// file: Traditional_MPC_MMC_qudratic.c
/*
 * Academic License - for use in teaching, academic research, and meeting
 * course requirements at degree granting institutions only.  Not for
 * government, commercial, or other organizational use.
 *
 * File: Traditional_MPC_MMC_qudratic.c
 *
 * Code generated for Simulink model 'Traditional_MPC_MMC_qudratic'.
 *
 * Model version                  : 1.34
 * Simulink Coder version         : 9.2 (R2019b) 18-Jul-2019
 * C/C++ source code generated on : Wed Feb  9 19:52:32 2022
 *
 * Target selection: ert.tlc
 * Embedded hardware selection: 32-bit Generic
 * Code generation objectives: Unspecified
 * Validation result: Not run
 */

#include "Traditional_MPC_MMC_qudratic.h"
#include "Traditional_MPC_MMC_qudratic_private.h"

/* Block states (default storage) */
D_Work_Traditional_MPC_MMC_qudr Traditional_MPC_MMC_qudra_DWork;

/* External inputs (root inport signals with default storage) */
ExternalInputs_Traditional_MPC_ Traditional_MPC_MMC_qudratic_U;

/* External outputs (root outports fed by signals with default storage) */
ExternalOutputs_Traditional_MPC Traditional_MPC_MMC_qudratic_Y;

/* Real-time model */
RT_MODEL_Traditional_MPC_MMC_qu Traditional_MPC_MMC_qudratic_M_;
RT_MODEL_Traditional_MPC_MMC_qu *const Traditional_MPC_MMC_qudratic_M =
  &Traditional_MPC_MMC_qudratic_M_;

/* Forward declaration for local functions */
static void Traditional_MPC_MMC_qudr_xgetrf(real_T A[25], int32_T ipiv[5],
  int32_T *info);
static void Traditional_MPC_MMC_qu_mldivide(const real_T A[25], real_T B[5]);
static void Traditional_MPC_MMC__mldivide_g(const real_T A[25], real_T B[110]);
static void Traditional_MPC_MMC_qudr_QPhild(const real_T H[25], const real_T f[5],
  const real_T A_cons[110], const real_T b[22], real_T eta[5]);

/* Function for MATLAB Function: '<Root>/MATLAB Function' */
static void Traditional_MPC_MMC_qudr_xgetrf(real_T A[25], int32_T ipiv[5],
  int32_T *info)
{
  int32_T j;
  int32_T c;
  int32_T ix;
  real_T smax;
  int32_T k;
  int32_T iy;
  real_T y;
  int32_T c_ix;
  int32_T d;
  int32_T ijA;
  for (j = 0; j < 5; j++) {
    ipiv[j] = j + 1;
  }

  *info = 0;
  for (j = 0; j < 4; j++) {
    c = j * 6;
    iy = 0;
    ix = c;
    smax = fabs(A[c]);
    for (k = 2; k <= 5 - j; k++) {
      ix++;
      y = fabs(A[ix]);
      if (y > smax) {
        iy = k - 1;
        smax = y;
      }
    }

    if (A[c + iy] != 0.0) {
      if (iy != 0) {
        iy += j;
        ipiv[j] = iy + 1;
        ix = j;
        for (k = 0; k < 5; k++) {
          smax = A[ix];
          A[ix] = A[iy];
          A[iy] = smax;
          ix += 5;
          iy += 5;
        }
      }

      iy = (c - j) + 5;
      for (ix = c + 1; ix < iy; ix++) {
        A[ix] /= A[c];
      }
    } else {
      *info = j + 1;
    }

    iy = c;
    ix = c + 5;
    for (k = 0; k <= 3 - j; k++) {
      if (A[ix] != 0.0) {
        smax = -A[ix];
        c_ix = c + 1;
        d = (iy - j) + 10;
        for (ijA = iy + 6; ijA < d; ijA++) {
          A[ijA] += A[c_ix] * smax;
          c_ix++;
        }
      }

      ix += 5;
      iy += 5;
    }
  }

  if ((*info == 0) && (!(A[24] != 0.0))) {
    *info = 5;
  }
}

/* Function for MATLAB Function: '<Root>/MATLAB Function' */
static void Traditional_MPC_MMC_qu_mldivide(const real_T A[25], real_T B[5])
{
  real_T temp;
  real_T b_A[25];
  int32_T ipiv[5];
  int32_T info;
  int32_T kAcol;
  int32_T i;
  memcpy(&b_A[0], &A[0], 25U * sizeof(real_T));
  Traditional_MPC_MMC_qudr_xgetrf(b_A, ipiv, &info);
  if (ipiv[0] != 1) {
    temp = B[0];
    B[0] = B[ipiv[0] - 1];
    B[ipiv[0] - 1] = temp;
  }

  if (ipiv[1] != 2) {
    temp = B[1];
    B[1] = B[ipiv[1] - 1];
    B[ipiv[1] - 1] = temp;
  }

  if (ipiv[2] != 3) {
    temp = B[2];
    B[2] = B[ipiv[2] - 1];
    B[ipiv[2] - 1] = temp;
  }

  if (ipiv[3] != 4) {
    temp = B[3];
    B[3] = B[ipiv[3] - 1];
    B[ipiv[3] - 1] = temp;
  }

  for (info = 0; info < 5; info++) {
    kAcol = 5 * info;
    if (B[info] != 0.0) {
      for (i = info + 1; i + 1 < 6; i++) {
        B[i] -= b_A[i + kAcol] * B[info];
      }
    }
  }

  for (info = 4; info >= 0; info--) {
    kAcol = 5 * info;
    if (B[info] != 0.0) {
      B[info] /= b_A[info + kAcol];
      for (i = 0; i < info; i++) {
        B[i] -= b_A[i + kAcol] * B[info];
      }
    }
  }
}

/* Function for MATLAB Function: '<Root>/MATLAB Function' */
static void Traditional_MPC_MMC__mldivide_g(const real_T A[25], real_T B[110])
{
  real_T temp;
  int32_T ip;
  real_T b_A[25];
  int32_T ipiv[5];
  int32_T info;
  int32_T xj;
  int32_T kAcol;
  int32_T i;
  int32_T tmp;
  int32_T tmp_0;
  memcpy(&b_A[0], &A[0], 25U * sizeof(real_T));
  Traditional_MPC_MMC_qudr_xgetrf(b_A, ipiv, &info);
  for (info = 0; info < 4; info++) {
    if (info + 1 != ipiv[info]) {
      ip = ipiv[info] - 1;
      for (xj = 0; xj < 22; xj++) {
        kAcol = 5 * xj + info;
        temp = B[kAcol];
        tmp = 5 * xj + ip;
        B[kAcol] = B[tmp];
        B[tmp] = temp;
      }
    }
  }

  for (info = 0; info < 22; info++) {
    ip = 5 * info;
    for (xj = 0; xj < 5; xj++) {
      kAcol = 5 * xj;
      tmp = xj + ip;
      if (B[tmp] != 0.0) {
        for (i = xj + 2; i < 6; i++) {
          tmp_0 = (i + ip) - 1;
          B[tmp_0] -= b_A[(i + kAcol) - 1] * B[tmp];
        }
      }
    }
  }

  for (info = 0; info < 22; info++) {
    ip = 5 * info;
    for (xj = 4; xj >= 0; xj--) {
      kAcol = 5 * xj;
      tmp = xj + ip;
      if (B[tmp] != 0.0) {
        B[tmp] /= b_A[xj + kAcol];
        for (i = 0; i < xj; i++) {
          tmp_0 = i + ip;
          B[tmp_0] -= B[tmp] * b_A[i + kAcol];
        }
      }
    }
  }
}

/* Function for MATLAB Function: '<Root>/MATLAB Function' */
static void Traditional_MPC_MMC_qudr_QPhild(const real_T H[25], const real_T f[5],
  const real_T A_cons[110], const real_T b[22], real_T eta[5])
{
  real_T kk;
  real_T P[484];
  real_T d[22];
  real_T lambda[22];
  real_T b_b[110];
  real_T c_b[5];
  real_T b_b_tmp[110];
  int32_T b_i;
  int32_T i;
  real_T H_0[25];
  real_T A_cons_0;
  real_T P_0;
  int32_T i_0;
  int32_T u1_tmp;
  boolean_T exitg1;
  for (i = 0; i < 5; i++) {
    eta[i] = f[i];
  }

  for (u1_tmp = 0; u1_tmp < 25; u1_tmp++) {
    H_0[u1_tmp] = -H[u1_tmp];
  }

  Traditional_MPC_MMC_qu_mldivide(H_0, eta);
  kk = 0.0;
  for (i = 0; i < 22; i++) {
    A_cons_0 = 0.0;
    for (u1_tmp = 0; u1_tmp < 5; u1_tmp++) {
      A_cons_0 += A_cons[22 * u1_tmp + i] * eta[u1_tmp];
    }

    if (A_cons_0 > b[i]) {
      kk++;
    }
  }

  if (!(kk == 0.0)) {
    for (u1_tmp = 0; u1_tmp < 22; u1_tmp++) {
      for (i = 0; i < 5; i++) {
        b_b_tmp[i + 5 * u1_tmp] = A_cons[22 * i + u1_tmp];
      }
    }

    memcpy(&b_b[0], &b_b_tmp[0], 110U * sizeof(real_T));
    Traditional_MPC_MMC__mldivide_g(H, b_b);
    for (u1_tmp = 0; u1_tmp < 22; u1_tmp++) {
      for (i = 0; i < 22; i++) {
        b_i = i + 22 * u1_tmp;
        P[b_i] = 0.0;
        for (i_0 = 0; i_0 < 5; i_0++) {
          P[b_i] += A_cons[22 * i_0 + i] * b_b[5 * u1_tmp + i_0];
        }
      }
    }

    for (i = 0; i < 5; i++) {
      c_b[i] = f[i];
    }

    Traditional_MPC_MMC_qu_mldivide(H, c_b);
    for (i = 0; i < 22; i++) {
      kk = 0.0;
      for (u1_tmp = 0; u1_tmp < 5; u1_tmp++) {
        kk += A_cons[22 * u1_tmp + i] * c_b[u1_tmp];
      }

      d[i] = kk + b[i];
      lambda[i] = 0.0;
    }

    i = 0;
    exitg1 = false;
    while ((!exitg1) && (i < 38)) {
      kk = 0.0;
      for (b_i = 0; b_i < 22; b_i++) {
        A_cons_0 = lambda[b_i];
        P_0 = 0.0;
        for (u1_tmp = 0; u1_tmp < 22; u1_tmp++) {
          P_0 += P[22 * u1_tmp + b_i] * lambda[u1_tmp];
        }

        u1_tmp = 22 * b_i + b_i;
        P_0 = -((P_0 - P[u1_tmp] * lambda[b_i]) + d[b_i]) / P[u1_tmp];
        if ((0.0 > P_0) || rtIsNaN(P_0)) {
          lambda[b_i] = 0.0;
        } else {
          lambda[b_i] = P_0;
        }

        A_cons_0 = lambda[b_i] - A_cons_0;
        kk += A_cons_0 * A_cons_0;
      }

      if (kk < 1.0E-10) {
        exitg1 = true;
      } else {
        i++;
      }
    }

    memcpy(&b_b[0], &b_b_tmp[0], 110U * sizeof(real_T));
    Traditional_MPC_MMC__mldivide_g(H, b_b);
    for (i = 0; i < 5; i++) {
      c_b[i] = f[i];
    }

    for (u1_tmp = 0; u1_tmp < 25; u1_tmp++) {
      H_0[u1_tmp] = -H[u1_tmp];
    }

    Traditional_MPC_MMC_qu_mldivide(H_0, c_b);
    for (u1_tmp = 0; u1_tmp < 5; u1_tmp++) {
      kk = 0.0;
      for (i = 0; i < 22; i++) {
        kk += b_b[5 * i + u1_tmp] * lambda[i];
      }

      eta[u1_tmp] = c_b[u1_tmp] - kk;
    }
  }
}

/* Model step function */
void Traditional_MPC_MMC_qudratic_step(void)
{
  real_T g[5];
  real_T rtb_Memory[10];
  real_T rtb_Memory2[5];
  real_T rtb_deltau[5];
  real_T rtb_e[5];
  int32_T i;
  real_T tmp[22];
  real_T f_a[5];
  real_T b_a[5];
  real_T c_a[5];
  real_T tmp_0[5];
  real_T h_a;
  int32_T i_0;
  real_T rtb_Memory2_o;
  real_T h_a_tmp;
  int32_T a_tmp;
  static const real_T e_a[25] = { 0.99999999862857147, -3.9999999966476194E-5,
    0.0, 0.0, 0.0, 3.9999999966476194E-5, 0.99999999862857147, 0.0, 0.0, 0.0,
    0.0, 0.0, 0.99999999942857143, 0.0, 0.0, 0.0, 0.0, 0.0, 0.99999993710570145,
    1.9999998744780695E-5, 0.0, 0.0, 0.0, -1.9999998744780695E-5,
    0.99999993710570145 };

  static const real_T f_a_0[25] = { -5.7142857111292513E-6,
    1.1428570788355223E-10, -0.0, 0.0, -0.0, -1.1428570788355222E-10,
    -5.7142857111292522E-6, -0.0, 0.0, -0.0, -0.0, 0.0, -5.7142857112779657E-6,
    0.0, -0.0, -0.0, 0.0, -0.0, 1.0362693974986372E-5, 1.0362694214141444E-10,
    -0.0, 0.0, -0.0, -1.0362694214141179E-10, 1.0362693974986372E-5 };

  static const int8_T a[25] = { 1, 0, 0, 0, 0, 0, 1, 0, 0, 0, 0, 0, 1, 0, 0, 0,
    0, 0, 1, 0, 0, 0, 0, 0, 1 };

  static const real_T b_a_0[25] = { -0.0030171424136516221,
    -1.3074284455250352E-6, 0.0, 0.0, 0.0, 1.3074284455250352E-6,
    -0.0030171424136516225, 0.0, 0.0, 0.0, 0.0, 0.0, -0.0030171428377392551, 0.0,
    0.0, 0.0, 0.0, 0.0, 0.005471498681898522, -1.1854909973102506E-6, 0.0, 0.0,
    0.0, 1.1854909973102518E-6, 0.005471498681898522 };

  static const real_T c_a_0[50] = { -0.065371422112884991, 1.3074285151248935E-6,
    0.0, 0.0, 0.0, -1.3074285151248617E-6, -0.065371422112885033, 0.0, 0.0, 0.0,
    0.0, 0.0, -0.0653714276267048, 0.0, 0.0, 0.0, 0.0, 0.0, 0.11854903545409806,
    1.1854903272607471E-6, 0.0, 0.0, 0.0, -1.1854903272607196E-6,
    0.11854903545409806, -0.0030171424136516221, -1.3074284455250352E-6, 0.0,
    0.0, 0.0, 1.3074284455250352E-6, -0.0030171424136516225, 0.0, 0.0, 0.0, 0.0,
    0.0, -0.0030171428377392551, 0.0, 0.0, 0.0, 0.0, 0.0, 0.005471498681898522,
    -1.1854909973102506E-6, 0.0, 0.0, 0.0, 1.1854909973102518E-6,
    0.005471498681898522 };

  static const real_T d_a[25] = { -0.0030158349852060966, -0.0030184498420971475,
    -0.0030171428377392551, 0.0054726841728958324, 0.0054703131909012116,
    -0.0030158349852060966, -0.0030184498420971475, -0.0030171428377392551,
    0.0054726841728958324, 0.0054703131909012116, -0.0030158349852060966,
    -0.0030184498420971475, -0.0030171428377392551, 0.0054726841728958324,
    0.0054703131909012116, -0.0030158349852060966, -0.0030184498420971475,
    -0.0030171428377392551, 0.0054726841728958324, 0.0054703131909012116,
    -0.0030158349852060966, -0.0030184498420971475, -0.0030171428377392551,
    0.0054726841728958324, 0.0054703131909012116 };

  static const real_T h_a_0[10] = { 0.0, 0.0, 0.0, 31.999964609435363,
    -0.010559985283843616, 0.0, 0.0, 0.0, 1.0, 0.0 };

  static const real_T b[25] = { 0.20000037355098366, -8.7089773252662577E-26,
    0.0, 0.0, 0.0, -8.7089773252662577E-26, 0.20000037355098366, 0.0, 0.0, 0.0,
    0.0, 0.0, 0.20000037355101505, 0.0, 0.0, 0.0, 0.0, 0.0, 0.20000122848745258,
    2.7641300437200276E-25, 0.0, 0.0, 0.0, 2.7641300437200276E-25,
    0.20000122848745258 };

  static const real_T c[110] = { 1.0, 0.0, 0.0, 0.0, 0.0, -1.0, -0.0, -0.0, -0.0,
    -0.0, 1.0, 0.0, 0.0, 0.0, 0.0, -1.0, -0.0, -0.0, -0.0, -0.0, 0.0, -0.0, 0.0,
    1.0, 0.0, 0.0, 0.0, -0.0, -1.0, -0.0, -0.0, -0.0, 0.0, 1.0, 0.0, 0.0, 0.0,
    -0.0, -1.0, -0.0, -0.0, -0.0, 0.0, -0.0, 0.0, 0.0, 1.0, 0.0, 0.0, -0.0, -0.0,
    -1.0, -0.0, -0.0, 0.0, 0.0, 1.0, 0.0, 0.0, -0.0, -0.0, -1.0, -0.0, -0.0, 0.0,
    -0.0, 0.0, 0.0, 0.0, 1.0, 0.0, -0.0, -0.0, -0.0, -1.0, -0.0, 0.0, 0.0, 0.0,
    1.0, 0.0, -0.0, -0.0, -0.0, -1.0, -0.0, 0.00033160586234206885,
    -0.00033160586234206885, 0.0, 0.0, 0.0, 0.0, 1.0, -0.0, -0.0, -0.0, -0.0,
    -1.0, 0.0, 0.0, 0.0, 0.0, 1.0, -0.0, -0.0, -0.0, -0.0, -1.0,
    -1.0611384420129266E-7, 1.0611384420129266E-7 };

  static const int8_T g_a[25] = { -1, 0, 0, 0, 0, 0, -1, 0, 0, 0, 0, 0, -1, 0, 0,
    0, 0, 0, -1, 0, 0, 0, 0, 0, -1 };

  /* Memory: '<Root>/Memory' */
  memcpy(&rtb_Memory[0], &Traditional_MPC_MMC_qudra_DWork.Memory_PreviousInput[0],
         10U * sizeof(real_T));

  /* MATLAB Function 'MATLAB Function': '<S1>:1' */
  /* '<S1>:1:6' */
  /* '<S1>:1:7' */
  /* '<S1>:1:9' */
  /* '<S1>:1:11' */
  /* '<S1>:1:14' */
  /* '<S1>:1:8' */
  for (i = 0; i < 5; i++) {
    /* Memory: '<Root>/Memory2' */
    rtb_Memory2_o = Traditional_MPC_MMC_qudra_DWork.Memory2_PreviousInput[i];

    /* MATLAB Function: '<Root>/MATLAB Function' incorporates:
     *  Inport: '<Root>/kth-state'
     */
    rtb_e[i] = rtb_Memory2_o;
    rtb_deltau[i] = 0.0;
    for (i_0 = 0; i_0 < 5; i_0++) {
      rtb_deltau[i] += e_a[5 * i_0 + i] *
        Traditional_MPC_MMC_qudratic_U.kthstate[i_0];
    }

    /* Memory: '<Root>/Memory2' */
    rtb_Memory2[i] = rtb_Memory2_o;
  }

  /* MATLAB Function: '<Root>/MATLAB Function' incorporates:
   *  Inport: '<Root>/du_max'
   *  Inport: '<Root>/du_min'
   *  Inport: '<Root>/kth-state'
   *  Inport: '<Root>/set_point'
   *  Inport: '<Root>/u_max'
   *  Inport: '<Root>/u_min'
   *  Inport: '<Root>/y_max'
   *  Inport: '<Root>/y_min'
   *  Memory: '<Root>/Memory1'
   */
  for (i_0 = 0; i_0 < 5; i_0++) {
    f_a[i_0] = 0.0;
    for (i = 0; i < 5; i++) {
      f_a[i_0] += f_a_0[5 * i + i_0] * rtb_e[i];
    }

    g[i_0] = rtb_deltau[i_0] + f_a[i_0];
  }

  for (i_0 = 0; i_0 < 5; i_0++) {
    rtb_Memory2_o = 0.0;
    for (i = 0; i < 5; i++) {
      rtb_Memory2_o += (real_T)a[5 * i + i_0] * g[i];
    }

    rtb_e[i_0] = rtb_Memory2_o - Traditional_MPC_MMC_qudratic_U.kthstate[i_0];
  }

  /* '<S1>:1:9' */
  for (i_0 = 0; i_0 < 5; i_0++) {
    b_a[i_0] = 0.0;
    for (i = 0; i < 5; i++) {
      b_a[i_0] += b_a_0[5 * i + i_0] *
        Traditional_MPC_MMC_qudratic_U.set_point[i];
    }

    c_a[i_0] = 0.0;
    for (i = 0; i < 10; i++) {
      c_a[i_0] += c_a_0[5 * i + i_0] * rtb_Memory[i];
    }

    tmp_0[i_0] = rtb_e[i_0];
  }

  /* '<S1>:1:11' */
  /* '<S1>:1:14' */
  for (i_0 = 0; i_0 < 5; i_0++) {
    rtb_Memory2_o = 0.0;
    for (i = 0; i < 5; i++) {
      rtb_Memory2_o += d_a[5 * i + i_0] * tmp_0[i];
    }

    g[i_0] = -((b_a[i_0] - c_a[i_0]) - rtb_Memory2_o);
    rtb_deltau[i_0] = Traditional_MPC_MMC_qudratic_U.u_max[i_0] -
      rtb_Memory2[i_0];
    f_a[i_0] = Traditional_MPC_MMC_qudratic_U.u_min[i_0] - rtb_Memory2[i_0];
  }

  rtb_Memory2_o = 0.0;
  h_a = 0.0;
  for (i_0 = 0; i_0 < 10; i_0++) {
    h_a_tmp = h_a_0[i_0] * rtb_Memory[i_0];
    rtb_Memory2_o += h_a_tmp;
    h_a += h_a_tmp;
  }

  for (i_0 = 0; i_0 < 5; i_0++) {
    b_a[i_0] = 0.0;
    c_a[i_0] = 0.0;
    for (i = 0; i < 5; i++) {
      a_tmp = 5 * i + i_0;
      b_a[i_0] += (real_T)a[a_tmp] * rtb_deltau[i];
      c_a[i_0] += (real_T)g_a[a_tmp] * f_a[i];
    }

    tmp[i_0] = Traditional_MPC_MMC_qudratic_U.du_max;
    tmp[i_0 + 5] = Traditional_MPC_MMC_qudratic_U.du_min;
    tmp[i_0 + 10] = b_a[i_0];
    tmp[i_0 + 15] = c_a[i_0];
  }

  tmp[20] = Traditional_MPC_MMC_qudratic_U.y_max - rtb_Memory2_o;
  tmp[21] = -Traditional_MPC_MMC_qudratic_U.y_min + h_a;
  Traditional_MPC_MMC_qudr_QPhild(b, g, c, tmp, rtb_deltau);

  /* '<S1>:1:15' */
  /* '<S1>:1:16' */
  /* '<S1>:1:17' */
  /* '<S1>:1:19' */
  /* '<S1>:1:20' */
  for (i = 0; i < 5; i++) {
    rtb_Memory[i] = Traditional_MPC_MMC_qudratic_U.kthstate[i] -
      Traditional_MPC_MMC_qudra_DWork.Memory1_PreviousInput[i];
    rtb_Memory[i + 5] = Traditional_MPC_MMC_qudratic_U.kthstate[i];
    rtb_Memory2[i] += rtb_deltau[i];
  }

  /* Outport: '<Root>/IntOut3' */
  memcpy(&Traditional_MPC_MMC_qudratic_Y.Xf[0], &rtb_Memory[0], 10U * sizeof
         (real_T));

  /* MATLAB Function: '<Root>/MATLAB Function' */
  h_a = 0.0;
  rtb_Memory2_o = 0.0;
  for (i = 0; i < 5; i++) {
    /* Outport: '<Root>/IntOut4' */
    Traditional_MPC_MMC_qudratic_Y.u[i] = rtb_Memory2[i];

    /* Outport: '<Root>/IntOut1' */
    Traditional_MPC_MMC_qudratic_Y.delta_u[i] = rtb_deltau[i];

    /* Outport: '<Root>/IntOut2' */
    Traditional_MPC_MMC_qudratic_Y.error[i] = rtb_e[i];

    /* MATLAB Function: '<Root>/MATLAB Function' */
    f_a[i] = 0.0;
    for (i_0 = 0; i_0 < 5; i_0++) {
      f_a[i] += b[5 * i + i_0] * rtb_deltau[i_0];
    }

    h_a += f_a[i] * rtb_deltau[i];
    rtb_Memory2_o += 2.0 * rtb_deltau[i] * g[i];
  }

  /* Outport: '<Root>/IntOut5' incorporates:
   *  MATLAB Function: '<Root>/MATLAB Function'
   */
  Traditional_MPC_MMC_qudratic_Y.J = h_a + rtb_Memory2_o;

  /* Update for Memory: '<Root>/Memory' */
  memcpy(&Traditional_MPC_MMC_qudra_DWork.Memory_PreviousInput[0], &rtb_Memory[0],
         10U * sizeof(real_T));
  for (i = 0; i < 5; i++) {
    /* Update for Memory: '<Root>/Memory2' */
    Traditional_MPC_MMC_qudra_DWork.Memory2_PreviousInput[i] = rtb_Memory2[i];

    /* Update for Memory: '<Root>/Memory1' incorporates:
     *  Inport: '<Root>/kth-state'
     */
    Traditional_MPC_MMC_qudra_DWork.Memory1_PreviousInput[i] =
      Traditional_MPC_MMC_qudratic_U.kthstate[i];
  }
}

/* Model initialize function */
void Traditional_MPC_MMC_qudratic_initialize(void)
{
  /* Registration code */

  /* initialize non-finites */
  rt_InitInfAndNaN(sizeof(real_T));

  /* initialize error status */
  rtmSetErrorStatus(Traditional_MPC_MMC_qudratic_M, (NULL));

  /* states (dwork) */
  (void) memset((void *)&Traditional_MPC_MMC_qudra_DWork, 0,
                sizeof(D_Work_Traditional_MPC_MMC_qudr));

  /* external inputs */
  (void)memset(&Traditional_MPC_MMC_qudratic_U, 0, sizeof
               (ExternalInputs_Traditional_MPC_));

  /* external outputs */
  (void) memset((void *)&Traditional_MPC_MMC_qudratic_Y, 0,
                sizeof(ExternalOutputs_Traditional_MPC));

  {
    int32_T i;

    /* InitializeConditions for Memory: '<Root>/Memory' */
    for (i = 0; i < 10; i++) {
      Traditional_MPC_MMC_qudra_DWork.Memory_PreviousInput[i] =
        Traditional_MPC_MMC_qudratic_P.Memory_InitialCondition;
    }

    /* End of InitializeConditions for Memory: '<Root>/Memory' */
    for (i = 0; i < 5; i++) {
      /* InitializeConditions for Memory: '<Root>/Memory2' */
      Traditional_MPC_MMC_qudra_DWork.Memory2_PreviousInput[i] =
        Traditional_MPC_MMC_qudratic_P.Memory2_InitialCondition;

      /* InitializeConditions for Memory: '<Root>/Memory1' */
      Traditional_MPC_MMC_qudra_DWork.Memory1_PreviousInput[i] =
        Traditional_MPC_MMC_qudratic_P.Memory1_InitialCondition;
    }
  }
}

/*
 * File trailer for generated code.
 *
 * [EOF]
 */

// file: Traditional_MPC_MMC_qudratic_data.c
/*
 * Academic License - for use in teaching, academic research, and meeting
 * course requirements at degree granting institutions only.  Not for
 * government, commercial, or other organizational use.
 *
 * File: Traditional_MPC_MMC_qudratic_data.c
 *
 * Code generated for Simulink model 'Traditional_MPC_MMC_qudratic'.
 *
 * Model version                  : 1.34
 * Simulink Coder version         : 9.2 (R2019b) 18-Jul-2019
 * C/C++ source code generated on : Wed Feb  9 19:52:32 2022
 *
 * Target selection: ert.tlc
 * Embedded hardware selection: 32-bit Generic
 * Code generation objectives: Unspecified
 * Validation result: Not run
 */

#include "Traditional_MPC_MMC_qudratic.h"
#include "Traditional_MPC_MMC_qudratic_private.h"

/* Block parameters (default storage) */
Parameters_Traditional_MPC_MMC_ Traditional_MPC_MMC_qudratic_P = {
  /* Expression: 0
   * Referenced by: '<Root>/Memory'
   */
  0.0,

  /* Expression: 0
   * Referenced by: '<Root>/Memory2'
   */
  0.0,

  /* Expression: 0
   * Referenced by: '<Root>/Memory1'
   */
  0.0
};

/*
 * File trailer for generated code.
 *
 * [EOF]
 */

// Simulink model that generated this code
simulink model "Traditional_MPC_MMC_qudratic"  (R2019b)
settings: Solver=ode3  StartTime=0.0  StopTime=3  FixedStep=0.000050  RelTol=1e-3  EnableMultiTasking=on

== system Traditional_MPC_MMC_qudratic ==
  set_point : Inport  PortDimensions=5
  kth-state : Inport  Port=2  PortDimensions=5
  u_max : Inport  Port=3  PortDimensions=5
  u_min : Inport  Port=4  PortDimensions=5
  du_max : Inport  Port=5  PortDimensions=1
  du_min : Inport  Port=6  PortDimensions=1
  y_max : Inport  Port=7  PortDimensions=1
  y_min : Inport  Port=8  PortDimensions=1
  MATLAB Function : MATLAB Function  TreatAsAtomicUnit=on
  Memory : Memory
  Memory1 : Memory
  Memory2 : Memory
  IntOut3 : Outport  SignalName=Xf
  IntOut4 : Outport  Port=2  SignalName=u
  IntOut1 : Outport  Port=3  SignalName=delta_u
  IntOut2 : Outport  Port=4  SignalName=error
  IntOut5 : Outport  Port=5  SignalName=J
  wires:
  set_point/1 -> MATLAB Function/1(r)
  MATLAB Function/1(Xf) -> IntOut3/1, Memory/1
  kth-state/1 -> MATLAB Function/2(xm_old), Memory1/1
  MATLAB Function/3(deltau) -> IntOut1/1
  Memory1/1 -> MATLAB Function/5(Xm_k_1)
  Memory/1 -> MATLAB Function/3(Xf_old)
  Memory2/1 -> MATLAB Function/4(u_old)
  MATLAB Function/2(u) -> Memory2/1, IntOut4/1
  u_max/1 -> MATLAB Function/6(u_max)
  u_min/1 -> MATLAB Function/7(u_min)
  MATLAB Function/4(e) -> IntOut2/1
  du_min/1 -> MATLAB Function/9(du_min)
  du_max/1 -> MATLAB Function/8(du_max)
  y_max/1 -> MATLAB Function/10(y_max)
  y_min/1 -> MATLAB Function/11(y_min)
  MATLAB Function/5(J) -> IntOut5/1

== matlab function Traditional_MPC_MMC_qudratic/MATLAB Function ==
function [Xf,u,deltau,e,J] = fcn(r,xm_old,Xf_old,u_old,Xm_k_1,u_max,u_min,du_max,du_min,y_max,y_min)
D = []; 
D= coder.load('initial_qudratic_paper_traditional_MPC.mat'); 

%%% model-plant mismatch error 
xm=D.Ap*xm_old+D.Bp*(u_old+D.up);
y_model=D.Cp*xm;
e = (y_model - xm_old); 
g = -(D.PhiT_Q_R_bar*r- D.PhiT_Q_F*(D.Xf+Xf_old)- D.PhiT_Q_Ie*(D.e+e)); 
%%% with one step output constraint there is no time over flow
B_LHS=[D.bduMax*du_max;-D.bduMin*du_min; D.Iu*(u_max-u_old);-D.Iu*(u_min-u_old);y_max-D.F(159,:)*(D.Xf+Xf_old);-y_min+D.F(159,:)*(D.Xf+Xf_old)]; %%F(4,:) indicate k+1 
%B_LHS=[D.bduMax*du_max;-D.bduMin*du_min; D.Iu*(u_max-u_old);-D.Iu*(u_min-u_old)];
%DeltaU = -D.H\g;
DeltaU = QPhild(D.H,g,D.C_LHS,B_LHS);
deltau= DeltaU(1:D.m,:);
J = DeltaU'*D.H*DeltaU + 2*DeltaU'*g;
u=D.up+u_old+deltau;
y = xm_old;
y_delta_k=y-Xm_k_1;
Xf=[y_delta_k;y];
end
